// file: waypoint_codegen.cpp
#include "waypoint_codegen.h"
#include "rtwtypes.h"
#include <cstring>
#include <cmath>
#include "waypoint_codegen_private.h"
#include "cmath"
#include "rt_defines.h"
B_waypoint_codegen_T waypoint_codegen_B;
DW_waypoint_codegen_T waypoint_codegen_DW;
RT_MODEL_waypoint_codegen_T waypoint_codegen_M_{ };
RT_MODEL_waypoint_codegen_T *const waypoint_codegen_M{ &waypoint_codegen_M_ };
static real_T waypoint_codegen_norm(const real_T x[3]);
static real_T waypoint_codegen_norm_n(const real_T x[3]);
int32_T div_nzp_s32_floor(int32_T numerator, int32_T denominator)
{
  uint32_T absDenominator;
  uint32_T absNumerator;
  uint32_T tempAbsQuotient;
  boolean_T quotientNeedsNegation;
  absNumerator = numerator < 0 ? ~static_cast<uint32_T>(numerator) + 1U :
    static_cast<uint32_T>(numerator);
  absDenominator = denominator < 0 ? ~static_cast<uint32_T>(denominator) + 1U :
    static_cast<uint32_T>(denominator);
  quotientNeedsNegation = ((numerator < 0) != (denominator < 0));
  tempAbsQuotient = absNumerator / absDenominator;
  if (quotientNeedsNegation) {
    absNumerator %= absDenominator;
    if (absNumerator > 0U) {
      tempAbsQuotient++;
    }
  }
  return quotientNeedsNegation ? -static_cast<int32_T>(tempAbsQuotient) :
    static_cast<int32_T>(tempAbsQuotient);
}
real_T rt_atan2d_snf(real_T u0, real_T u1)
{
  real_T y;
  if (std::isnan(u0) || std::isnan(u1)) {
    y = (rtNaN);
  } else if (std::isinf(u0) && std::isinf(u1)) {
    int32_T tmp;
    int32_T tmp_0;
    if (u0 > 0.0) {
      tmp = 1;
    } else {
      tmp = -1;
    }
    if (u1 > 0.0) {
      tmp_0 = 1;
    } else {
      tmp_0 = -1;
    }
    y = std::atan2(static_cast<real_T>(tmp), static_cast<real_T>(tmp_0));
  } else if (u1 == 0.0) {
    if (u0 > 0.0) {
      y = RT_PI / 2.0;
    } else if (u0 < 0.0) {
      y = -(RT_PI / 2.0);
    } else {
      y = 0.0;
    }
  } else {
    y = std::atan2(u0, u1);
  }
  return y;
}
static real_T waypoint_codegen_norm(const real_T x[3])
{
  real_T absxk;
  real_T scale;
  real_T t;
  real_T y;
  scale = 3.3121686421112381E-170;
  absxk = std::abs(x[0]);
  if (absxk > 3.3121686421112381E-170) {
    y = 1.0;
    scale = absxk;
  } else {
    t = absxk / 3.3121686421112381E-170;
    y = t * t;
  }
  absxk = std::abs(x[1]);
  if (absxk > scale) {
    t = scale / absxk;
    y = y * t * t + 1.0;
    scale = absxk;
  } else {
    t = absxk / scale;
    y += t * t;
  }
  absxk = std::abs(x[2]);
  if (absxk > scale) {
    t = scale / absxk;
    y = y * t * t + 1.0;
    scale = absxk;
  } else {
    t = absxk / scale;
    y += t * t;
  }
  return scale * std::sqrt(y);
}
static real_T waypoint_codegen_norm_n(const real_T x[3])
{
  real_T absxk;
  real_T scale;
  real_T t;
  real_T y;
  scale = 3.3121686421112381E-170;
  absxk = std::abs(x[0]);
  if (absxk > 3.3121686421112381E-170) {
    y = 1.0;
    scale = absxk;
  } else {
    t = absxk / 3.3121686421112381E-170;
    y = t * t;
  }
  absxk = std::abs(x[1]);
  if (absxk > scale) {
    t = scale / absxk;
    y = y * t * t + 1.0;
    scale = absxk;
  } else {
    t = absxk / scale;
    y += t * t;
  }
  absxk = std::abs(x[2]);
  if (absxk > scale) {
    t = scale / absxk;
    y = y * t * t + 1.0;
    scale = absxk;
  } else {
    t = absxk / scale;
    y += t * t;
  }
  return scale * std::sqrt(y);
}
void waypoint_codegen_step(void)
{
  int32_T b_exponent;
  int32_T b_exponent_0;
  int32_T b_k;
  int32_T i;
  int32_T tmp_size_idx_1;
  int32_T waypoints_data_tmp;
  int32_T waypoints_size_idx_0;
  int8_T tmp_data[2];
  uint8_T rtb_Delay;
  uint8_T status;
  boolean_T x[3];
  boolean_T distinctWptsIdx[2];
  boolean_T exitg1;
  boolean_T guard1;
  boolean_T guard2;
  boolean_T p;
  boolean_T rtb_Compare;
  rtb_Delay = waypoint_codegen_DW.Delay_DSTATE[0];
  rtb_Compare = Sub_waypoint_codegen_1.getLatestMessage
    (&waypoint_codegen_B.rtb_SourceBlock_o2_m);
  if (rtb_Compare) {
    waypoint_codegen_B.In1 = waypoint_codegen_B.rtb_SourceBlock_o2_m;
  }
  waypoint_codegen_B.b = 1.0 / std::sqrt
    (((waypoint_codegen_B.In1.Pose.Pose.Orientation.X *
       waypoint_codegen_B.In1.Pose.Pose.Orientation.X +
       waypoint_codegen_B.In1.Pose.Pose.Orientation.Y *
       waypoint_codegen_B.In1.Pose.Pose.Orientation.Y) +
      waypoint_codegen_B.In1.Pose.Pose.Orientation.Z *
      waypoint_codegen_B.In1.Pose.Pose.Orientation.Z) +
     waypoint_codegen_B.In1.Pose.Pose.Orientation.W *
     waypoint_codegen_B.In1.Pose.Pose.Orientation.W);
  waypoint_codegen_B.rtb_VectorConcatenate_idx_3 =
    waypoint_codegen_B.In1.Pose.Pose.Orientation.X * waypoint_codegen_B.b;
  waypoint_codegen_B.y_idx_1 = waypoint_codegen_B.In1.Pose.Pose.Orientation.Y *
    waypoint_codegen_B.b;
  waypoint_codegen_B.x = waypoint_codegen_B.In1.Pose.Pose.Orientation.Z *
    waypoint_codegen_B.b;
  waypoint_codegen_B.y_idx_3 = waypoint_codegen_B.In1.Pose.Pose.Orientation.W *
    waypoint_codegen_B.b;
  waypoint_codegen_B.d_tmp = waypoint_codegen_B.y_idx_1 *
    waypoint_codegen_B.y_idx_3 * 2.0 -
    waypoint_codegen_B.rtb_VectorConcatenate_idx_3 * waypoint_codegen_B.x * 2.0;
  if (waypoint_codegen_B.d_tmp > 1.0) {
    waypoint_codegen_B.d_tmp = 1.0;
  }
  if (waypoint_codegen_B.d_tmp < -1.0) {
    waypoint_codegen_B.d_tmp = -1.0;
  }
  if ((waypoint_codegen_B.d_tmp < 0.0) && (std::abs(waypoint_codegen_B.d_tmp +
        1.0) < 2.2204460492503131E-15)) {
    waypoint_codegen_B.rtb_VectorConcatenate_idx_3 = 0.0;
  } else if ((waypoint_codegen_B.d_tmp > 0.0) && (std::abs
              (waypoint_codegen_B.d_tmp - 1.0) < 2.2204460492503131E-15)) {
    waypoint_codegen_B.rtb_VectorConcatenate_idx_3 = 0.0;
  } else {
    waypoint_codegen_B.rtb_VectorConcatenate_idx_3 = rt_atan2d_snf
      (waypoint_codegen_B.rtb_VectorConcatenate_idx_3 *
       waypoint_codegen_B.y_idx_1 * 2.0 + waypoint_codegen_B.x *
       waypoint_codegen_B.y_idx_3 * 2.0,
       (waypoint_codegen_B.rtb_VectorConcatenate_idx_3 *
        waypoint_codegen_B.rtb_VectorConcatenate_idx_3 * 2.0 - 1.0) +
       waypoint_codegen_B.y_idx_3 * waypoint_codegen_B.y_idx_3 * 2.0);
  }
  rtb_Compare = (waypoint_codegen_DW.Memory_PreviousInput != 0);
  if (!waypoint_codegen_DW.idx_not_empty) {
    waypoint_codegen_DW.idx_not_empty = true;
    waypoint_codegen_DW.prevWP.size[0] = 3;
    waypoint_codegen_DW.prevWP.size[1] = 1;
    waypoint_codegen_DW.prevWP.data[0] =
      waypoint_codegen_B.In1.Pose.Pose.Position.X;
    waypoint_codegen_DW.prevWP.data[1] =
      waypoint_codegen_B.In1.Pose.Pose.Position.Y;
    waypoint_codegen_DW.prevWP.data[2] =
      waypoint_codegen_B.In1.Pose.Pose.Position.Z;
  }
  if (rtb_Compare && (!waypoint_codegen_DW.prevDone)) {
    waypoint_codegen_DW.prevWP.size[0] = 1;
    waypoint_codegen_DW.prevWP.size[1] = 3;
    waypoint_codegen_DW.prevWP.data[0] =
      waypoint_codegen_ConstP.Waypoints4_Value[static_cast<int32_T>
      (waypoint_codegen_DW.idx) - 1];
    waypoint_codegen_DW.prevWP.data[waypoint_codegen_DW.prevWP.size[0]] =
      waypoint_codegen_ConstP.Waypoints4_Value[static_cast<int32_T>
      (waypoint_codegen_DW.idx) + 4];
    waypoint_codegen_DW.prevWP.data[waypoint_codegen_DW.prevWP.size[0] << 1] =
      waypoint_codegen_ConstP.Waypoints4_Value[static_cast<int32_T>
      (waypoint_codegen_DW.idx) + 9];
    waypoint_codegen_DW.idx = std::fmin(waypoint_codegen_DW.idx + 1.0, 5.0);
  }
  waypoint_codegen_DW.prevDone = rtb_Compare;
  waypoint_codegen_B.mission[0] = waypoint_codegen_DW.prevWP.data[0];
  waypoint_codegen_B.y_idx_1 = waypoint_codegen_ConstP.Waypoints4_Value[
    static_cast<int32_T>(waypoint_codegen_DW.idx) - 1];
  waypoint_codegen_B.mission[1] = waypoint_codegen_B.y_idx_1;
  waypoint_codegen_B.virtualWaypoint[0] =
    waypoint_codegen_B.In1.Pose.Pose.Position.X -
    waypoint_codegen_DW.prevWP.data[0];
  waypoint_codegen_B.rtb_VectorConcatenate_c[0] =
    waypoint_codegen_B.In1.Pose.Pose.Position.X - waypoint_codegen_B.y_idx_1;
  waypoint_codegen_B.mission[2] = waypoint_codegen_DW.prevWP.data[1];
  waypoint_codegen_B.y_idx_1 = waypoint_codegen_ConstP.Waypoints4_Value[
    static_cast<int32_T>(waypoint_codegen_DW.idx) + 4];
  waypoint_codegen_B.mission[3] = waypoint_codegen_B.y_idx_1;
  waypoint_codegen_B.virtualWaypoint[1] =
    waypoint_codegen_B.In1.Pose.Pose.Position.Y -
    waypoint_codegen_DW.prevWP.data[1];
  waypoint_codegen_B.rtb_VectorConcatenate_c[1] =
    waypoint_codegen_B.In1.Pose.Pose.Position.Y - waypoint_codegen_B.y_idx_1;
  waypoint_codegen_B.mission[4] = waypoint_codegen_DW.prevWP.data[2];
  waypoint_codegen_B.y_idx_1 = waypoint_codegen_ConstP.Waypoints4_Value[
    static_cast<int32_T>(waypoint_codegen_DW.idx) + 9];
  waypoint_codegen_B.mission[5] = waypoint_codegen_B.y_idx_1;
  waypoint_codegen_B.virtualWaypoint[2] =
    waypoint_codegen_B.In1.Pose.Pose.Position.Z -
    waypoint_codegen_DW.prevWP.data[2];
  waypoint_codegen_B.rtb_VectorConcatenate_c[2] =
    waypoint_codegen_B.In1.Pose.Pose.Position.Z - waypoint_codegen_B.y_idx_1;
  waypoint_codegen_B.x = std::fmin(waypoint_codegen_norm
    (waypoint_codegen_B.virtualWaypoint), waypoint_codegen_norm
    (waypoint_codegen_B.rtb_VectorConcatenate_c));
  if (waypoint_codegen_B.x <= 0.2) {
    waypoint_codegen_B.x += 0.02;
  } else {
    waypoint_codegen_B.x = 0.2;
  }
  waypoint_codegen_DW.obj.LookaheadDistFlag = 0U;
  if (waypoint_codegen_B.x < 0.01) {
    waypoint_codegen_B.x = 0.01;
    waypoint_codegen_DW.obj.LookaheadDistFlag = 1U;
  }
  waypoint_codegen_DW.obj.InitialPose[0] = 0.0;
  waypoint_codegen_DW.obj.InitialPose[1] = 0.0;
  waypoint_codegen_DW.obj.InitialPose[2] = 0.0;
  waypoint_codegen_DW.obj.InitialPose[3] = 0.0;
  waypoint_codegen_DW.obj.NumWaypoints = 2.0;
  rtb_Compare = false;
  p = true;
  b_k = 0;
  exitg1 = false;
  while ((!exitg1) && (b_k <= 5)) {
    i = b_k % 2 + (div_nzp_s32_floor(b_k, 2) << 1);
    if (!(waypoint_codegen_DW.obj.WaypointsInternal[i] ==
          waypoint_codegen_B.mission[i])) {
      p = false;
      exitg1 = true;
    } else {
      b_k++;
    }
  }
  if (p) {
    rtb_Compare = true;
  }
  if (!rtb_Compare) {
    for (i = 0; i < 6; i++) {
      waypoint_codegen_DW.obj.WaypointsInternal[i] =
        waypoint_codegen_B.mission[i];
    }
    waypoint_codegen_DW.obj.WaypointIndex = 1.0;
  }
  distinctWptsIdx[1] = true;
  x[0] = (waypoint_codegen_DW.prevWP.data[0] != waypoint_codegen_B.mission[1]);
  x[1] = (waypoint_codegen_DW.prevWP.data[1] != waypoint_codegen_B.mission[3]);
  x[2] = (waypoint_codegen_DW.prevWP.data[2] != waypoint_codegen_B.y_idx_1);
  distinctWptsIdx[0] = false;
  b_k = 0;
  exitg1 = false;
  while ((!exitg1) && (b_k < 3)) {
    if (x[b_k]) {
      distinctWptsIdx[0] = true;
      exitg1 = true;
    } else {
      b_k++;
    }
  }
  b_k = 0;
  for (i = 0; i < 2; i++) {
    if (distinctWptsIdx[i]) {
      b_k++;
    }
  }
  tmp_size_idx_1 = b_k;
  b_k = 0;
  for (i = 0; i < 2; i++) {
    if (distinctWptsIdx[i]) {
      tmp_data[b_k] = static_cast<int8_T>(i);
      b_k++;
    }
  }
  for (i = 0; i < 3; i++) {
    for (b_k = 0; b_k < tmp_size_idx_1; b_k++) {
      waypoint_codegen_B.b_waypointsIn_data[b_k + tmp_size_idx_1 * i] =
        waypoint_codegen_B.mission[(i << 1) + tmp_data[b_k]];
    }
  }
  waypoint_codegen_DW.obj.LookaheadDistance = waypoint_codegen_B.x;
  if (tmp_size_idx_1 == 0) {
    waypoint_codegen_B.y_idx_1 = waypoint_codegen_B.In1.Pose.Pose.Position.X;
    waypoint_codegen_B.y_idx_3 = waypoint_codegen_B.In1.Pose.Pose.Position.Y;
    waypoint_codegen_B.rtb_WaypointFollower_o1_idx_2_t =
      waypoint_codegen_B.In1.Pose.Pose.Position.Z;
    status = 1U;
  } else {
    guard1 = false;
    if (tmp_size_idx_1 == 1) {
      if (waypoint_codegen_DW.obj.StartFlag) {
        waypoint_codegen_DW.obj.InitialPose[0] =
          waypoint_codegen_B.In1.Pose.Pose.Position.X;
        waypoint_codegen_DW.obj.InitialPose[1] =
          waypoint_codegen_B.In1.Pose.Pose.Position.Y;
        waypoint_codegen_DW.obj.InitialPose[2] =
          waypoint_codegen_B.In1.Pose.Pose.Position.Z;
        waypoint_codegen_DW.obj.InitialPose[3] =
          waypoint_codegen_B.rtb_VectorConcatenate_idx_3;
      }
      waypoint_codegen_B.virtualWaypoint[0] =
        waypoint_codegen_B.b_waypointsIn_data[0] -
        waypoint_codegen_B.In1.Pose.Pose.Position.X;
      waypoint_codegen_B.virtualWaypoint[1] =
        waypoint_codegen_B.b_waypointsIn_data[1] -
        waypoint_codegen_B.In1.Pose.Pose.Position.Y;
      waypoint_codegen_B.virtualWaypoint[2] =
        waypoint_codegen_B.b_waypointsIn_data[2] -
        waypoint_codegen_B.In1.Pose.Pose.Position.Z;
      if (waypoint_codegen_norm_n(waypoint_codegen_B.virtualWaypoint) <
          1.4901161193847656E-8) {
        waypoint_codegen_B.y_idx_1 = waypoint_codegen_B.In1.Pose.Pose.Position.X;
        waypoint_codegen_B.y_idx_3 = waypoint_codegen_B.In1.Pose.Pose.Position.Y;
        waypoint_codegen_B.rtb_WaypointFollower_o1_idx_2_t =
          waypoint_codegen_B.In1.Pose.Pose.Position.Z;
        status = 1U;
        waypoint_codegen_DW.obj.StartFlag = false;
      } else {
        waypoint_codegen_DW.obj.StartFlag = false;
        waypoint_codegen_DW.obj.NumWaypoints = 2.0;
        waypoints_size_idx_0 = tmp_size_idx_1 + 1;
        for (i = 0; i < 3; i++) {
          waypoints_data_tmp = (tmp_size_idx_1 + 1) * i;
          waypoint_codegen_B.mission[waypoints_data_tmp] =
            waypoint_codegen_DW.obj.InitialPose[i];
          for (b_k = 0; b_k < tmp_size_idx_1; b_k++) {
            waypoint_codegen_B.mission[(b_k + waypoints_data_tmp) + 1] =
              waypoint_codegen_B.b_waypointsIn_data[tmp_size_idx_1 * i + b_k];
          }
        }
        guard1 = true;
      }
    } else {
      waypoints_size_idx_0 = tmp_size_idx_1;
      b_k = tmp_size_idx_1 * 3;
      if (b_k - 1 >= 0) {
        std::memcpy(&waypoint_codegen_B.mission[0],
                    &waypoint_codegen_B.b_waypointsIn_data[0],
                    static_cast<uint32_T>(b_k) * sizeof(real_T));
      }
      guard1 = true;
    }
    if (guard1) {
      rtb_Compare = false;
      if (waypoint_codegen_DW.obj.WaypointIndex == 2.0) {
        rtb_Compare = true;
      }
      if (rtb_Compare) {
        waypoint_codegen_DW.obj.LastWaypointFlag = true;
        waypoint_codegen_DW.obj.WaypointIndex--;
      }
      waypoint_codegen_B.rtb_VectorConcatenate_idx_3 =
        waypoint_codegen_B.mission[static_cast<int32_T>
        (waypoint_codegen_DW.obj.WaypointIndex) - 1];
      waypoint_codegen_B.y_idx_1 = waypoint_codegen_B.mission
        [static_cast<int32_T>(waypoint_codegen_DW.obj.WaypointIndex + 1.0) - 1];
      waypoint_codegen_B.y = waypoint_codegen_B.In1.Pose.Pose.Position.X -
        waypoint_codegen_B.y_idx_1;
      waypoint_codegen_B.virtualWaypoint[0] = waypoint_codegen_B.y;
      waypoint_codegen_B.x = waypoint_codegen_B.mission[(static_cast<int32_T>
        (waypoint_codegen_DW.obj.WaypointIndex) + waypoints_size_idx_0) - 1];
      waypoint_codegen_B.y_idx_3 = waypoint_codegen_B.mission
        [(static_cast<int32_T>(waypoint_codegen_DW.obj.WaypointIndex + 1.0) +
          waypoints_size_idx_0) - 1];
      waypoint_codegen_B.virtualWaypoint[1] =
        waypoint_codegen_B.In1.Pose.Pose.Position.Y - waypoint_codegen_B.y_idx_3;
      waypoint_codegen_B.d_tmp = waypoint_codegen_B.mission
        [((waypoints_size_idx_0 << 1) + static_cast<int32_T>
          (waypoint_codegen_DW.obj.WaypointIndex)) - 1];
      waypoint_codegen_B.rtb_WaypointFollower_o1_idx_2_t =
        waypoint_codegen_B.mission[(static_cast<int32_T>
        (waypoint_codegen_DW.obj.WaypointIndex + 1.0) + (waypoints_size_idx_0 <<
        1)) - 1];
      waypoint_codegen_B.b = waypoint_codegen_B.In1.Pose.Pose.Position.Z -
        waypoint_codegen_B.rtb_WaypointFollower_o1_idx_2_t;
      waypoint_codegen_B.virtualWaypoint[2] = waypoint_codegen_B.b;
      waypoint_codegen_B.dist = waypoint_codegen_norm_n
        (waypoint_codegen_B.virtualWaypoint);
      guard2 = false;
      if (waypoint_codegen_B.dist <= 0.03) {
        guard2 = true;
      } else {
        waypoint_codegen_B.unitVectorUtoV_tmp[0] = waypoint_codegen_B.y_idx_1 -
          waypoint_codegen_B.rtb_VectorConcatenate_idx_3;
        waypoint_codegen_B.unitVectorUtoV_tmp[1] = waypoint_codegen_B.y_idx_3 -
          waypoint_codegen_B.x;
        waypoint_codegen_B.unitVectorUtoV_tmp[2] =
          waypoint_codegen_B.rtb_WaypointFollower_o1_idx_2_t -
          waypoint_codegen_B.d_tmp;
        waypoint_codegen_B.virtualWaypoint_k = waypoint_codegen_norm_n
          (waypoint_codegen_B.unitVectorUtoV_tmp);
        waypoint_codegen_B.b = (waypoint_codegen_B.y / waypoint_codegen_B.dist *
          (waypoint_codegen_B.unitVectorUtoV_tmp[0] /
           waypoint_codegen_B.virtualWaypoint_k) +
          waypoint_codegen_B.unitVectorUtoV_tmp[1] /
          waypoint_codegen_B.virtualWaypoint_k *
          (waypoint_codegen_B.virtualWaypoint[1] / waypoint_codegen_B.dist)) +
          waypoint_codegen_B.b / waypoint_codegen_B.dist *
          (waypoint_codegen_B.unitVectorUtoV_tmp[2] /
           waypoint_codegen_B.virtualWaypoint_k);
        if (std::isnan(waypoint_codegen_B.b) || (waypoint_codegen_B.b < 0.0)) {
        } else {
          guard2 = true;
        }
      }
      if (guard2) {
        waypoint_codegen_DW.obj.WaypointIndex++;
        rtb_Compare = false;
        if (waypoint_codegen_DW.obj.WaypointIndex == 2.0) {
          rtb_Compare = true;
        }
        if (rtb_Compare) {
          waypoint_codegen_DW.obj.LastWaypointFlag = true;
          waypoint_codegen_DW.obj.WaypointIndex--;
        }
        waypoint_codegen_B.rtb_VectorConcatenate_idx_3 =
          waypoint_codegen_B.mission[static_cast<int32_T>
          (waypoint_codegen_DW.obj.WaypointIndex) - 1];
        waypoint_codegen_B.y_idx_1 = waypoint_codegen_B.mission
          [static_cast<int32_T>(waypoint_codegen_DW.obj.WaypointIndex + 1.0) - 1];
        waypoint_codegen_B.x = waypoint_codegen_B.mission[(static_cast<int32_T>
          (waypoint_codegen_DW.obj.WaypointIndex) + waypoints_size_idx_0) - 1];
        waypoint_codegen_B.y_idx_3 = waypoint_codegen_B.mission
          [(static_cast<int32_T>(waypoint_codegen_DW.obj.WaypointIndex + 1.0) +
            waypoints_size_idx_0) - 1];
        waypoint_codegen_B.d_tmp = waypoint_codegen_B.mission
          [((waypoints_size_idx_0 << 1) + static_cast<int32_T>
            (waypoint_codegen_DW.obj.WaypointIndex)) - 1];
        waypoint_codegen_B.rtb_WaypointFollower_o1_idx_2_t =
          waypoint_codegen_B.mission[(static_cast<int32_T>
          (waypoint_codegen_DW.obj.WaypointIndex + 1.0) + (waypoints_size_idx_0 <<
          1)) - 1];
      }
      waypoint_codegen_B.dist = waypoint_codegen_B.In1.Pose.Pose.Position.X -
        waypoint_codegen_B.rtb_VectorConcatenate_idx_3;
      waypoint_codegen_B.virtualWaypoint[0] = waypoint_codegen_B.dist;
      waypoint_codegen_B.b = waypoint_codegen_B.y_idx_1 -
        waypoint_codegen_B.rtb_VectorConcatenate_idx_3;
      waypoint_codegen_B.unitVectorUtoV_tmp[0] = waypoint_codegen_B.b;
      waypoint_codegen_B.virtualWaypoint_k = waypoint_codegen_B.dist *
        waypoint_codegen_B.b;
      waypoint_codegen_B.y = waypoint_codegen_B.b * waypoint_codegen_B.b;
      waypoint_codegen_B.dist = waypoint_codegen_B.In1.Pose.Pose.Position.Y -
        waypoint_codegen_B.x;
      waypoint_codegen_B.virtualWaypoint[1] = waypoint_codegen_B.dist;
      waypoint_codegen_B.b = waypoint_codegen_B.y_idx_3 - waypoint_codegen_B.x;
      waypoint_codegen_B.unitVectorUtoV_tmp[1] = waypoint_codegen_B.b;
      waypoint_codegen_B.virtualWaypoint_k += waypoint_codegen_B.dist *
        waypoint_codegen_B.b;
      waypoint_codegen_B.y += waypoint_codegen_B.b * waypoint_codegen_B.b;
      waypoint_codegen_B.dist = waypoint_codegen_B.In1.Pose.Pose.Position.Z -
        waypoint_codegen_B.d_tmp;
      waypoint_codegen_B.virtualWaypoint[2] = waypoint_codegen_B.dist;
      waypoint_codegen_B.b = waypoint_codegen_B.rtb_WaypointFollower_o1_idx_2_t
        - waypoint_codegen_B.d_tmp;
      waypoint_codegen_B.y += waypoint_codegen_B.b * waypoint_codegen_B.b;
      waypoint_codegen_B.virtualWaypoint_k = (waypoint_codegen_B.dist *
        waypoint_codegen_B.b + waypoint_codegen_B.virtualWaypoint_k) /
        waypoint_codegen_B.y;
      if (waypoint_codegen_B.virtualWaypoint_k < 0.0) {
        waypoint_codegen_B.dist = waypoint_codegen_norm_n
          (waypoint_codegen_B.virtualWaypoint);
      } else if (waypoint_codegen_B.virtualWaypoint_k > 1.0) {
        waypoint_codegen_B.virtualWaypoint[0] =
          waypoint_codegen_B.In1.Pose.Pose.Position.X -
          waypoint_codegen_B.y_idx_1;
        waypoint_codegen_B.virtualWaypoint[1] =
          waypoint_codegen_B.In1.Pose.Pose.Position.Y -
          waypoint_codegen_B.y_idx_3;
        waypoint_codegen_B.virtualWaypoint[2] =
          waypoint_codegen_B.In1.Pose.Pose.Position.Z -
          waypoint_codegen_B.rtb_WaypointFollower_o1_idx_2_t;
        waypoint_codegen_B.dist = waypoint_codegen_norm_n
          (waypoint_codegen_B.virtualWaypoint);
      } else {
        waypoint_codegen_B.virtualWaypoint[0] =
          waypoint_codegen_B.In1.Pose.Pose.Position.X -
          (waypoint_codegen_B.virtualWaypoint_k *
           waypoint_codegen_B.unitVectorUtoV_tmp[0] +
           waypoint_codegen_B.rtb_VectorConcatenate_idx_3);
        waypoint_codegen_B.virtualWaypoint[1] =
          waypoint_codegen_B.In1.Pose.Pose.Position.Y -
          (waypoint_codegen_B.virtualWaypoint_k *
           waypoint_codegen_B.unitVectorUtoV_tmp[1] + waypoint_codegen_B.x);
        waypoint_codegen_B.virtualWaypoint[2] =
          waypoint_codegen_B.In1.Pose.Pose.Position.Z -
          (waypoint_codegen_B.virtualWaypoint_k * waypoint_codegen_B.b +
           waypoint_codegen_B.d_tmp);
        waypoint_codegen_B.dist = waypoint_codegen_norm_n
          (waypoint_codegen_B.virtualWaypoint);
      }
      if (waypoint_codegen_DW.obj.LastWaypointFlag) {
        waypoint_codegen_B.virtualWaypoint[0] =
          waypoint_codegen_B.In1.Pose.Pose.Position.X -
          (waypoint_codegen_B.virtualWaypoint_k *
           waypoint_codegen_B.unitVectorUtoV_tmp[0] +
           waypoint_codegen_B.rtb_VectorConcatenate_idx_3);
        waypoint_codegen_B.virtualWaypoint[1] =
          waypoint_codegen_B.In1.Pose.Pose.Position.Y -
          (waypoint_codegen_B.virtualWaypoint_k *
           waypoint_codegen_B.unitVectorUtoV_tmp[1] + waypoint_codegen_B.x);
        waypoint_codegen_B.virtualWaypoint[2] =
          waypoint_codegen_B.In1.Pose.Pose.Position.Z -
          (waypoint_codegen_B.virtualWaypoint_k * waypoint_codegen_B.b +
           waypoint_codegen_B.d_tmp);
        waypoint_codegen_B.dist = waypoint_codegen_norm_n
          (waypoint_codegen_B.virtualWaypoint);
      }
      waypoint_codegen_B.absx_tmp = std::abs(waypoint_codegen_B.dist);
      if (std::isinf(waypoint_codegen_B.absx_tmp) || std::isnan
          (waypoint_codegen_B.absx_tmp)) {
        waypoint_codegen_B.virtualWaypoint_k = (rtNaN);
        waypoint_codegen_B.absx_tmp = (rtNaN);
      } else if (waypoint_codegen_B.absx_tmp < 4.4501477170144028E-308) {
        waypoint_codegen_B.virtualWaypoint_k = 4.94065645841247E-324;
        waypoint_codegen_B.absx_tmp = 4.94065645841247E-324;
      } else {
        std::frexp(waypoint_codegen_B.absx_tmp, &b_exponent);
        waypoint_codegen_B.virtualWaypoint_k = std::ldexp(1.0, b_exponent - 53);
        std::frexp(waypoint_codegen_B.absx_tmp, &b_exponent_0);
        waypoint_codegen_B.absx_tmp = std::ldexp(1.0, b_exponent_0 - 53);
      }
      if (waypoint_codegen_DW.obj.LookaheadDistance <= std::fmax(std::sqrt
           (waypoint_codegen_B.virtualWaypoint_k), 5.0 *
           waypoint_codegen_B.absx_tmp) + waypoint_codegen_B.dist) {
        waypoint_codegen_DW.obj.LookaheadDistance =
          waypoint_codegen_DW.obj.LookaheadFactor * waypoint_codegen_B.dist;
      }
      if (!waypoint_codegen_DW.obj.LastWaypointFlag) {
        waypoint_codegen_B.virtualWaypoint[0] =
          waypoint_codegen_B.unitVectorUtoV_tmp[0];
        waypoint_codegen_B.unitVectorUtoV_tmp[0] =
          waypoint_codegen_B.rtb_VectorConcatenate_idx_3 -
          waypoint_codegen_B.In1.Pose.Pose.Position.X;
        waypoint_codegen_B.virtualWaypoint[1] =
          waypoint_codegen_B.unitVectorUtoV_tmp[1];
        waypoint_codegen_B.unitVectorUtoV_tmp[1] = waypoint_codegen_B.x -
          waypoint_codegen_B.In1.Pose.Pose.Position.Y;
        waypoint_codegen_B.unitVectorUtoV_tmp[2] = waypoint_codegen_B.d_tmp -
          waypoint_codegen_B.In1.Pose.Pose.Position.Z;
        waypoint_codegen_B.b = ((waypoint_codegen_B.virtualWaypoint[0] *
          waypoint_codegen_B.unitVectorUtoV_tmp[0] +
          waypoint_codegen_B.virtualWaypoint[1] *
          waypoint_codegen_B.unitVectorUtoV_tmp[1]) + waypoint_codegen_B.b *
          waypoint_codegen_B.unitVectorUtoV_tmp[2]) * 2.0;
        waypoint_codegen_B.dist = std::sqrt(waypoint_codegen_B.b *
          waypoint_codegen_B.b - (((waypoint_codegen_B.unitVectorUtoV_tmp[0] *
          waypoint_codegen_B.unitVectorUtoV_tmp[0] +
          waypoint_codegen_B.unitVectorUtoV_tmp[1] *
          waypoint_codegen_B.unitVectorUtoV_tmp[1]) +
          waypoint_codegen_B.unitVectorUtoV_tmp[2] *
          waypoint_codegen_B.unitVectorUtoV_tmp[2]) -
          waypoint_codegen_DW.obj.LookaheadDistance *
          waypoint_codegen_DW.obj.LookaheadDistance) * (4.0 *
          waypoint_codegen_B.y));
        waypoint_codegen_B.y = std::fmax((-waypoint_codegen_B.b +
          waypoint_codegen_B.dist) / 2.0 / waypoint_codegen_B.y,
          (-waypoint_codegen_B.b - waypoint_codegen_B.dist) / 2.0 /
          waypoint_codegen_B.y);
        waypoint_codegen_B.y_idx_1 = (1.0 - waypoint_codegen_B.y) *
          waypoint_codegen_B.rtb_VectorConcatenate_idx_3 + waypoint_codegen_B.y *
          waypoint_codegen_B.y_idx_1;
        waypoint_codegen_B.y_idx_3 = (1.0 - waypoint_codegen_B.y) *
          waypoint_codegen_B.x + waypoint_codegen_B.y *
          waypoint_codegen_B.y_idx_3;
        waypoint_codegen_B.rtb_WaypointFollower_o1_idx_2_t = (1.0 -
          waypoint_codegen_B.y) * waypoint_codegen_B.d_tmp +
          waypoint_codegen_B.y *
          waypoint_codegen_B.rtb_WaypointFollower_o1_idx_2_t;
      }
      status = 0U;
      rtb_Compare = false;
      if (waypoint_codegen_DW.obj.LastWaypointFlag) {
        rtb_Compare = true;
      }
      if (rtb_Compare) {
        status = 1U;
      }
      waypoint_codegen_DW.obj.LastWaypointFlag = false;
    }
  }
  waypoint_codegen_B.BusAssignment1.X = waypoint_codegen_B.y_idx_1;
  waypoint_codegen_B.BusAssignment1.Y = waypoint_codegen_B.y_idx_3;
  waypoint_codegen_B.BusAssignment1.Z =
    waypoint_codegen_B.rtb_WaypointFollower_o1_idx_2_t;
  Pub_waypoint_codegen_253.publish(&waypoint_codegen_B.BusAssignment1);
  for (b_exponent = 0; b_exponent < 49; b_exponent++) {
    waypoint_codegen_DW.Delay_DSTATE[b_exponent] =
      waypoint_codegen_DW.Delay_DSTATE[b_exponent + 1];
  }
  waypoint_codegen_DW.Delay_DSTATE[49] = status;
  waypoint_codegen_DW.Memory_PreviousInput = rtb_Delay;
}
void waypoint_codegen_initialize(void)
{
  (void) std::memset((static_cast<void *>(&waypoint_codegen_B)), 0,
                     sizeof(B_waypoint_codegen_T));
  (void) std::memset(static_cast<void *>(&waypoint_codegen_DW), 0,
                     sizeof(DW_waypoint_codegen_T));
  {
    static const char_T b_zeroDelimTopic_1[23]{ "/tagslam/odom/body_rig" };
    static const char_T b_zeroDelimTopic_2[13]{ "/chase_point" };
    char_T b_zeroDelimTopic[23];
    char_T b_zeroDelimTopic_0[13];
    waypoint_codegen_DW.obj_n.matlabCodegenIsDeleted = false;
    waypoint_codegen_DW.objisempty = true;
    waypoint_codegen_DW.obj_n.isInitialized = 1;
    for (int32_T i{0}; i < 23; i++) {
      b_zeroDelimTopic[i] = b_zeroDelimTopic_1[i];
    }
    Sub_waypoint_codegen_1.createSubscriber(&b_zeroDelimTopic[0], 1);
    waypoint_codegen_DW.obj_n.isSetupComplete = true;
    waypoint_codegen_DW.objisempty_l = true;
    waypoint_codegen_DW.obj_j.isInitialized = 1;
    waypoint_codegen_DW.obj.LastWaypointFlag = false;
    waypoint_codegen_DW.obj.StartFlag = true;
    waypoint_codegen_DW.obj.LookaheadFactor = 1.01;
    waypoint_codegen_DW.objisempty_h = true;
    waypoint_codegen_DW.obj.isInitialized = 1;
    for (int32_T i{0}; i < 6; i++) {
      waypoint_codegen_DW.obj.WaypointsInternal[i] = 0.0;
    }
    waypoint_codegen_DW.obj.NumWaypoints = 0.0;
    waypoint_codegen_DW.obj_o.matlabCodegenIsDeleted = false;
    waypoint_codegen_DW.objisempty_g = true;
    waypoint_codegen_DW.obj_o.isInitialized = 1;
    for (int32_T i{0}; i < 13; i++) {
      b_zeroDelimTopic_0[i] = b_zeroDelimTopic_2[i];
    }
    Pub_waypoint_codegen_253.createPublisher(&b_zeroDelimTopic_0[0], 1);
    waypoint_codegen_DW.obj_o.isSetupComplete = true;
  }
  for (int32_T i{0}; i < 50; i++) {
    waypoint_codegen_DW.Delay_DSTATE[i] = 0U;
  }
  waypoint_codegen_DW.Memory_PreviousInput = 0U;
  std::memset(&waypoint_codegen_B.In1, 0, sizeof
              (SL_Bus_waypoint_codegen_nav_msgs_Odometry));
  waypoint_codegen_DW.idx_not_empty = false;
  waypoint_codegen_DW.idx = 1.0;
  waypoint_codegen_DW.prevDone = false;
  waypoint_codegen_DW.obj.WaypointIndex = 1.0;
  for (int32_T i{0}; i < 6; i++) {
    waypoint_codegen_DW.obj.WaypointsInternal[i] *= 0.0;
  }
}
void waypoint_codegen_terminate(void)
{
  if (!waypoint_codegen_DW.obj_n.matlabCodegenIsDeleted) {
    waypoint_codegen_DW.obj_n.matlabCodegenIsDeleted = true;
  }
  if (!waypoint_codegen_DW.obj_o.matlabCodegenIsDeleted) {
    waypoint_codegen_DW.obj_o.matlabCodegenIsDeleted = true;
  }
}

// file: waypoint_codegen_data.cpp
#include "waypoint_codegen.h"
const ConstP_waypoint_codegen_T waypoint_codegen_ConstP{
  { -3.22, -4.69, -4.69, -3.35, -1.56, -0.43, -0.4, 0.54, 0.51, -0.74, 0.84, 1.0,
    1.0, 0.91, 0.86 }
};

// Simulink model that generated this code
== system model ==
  Publish#1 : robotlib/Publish  <- 1: BusAssignment1
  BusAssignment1 : BusAssignment  <- 1: BlankMessage#1, 2: Selector#1, 3: Selector#2, 4: Selector#3
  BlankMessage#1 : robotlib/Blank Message
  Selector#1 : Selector  Indices=[0]  <- 1: WaypointFollower
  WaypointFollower : uavalgslib/Waypoint Follower  <- 1: VectorConcatenate, 2: MATLABFunction#1, 3: MATLABFunction#2
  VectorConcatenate : Concatenate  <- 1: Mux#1, 2: Selector#4
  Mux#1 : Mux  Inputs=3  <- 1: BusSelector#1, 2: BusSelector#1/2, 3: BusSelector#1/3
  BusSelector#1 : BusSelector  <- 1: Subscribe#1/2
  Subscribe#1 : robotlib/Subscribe
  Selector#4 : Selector  Indices=[3]  <- 1: CoordinateTransformationConversion#1
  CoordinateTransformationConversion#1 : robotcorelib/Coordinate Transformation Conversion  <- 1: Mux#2
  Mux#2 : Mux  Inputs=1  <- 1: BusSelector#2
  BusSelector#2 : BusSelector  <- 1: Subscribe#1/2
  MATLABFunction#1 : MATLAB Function  <- 1: Waypoints4, 2: Selector#5, 3: CompareToZero#1
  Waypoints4 : Constant  Value=[-3.22,-0.43,0.84; -4.69, -0.40, 1.00; -4.69, 0.54, 1.00; -3.35, 0.51, 0.91; -1.56,-0.74, 0.86]
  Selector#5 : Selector  Indices=[1 2 3]  <- 1: VectorConcatenate
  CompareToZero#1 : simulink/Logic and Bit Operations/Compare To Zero  relop=~=  <- 1: Memory
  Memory : Memory  <- 1: Delay
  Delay : Delay  DelayLength=50  <- 1: WaypointFollower/6
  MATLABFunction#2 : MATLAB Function  <- 1: MATLABFunction#1, 2: Math#1, 3: Constant#1
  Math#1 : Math  Operator=transpose  <- 1: Selector#5
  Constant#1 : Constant  Value=0.2
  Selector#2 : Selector  Indices=[1]  <- 1: WaypointFollower
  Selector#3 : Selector  Indices=[2]  <- 1: WaypointFollower
== matlab function MATLABFunction#2 ==
function d = decayDebug(wp_pair, position, lookAheadDistance)
%#codegen
prevWP = wp_pair(1,:);
nextWP = wp_pair(2,:);

distToStart = norm(position - prevWP);
distToEnd   = norm(position - nextWP);

x = min(distToStart, distToEnd);

if x <= lookAheadDistance
    d = x + 0.02;
else
    d = lookAheadDistance;

end

end

== matlab function MATLABFunction#1 ==
% MATLAB Function Block: generateMission
% Inputs:
%   waypoints   - Nx3 matrix of [x y z] waypoints
%   pose        - 1x3 current [x y z] position
%   isDone      - scalar (0 or 1), indicates waypoint reached
% Output:
%   mission     - 2x3 matrix: [previous_wp; target_wp]

function mission = generateMission(waypoints, pose, isDone)
%#codegen
% Preallocate output for codegen
mission = zeros(2,3,'like',waypoints);

persistent idx prevWP prevDone nWPs

% Initialize or reset on waypoint count change
if isempty(nWPs)
    nWPs = size(waypoints,1);
end
if isempty(idx) || nWPs ~= size(waypoints,1)
    idx      = 1;
    prevWP   = pose;       % start from initial pose
    prevDone = false;
    nWPs     = size(waypoints,1);
end

% Detect rising edge of isDone
if isDone && ~prevDone

    % Advance previous to current target
    prevWP = waypoints(idx, :);
    % Increment index, cap at end
    idx = min(idx + 1, nWPs);
end
% Store current isDone state
prevDone = isDone;

% Output previous and current target waypoints
mission(1, :) = prevWP;
mission(2, :) = waypoints(idx, :);
end
